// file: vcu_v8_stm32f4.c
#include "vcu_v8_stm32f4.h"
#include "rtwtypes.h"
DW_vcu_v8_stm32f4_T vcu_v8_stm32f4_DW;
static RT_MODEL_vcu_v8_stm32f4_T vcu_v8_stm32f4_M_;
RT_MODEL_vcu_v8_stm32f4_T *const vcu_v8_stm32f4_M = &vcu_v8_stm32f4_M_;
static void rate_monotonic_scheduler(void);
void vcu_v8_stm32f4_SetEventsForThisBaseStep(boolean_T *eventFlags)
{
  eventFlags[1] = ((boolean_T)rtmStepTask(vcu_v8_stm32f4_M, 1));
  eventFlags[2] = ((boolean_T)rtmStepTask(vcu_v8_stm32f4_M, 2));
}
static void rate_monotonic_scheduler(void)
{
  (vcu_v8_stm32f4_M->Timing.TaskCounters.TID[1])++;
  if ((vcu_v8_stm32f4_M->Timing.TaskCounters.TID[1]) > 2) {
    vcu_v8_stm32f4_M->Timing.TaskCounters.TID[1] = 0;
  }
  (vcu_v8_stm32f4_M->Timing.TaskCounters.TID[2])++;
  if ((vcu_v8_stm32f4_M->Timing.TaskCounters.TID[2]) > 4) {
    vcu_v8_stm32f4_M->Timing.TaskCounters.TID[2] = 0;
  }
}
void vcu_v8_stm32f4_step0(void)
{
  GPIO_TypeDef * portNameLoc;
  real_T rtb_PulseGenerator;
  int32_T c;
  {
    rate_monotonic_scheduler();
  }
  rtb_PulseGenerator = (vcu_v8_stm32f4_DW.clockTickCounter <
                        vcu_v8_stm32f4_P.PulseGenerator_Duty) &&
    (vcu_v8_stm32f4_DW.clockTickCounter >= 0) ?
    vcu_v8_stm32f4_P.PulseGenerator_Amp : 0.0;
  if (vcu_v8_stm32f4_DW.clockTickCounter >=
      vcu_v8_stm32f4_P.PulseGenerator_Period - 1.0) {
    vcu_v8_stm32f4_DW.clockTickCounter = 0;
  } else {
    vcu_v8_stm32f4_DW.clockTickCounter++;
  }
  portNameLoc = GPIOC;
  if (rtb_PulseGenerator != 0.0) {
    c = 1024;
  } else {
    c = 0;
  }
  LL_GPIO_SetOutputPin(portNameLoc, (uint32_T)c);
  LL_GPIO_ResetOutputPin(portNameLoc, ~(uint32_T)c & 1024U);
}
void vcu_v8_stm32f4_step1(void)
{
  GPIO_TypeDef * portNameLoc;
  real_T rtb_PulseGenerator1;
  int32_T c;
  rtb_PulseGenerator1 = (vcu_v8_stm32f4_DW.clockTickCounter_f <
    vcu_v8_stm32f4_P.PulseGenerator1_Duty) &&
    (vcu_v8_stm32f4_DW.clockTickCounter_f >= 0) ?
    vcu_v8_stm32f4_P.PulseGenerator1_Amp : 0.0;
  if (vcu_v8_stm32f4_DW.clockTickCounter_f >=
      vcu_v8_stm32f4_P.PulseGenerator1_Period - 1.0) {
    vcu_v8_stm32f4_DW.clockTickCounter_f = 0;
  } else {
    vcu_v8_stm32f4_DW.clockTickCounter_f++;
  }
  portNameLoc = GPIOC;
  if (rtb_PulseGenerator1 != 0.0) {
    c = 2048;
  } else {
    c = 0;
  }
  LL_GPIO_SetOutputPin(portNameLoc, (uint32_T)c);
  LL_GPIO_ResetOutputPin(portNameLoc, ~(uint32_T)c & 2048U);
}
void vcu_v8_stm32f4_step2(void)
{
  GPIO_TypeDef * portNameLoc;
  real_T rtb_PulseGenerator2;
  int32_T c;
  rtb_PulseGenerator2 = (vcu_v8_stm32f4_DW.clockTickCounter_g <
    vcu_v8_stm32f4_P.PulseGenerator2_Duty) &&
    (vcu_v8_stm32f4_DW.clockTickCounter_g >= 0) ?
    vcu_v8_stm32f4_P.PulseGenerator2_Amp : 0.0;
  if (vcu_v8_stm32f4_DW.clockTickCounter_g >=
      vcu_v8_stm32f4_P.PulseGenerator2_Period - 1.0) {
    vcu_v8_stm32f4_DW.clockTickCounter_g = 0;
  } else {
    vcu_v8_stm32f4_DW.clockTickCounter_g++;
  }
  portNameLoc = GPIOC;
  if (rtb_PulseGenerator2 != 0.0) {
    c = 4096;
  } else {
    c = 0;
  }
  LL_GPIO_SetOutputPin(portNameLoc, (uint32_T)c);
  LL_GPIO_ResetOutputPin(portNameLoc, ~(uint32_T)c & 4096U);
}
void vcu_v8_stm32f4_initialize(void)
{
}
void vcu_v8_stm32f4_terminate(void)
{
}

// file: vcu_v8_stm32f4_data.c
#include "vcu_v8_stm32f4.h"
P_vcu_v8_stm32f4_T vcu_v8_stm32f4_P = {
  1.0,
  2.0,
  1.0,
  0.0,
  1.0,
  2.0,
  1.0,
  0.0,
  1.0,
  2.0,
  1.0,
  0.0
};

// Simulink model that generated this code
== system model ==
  DigitalPortWrite#1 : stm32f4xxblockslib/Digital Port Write  <- 1: PulseGenerator
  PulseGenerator : DiscretePulseGenerator  Period=1  PulseWidth=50
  DigitalPortWrite#2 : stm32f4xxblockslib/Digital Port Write  <- 1: PulseGenerator1
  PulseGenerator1 : DiscretePulseGenerator  Period=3  PulseWidth=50
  DigitalPortWrite#3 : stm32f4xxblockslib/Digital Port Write  <- 1: PulseGenerator2
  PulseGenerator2 : DiscretePulseGenerator  Period=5  PulseWidth=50
